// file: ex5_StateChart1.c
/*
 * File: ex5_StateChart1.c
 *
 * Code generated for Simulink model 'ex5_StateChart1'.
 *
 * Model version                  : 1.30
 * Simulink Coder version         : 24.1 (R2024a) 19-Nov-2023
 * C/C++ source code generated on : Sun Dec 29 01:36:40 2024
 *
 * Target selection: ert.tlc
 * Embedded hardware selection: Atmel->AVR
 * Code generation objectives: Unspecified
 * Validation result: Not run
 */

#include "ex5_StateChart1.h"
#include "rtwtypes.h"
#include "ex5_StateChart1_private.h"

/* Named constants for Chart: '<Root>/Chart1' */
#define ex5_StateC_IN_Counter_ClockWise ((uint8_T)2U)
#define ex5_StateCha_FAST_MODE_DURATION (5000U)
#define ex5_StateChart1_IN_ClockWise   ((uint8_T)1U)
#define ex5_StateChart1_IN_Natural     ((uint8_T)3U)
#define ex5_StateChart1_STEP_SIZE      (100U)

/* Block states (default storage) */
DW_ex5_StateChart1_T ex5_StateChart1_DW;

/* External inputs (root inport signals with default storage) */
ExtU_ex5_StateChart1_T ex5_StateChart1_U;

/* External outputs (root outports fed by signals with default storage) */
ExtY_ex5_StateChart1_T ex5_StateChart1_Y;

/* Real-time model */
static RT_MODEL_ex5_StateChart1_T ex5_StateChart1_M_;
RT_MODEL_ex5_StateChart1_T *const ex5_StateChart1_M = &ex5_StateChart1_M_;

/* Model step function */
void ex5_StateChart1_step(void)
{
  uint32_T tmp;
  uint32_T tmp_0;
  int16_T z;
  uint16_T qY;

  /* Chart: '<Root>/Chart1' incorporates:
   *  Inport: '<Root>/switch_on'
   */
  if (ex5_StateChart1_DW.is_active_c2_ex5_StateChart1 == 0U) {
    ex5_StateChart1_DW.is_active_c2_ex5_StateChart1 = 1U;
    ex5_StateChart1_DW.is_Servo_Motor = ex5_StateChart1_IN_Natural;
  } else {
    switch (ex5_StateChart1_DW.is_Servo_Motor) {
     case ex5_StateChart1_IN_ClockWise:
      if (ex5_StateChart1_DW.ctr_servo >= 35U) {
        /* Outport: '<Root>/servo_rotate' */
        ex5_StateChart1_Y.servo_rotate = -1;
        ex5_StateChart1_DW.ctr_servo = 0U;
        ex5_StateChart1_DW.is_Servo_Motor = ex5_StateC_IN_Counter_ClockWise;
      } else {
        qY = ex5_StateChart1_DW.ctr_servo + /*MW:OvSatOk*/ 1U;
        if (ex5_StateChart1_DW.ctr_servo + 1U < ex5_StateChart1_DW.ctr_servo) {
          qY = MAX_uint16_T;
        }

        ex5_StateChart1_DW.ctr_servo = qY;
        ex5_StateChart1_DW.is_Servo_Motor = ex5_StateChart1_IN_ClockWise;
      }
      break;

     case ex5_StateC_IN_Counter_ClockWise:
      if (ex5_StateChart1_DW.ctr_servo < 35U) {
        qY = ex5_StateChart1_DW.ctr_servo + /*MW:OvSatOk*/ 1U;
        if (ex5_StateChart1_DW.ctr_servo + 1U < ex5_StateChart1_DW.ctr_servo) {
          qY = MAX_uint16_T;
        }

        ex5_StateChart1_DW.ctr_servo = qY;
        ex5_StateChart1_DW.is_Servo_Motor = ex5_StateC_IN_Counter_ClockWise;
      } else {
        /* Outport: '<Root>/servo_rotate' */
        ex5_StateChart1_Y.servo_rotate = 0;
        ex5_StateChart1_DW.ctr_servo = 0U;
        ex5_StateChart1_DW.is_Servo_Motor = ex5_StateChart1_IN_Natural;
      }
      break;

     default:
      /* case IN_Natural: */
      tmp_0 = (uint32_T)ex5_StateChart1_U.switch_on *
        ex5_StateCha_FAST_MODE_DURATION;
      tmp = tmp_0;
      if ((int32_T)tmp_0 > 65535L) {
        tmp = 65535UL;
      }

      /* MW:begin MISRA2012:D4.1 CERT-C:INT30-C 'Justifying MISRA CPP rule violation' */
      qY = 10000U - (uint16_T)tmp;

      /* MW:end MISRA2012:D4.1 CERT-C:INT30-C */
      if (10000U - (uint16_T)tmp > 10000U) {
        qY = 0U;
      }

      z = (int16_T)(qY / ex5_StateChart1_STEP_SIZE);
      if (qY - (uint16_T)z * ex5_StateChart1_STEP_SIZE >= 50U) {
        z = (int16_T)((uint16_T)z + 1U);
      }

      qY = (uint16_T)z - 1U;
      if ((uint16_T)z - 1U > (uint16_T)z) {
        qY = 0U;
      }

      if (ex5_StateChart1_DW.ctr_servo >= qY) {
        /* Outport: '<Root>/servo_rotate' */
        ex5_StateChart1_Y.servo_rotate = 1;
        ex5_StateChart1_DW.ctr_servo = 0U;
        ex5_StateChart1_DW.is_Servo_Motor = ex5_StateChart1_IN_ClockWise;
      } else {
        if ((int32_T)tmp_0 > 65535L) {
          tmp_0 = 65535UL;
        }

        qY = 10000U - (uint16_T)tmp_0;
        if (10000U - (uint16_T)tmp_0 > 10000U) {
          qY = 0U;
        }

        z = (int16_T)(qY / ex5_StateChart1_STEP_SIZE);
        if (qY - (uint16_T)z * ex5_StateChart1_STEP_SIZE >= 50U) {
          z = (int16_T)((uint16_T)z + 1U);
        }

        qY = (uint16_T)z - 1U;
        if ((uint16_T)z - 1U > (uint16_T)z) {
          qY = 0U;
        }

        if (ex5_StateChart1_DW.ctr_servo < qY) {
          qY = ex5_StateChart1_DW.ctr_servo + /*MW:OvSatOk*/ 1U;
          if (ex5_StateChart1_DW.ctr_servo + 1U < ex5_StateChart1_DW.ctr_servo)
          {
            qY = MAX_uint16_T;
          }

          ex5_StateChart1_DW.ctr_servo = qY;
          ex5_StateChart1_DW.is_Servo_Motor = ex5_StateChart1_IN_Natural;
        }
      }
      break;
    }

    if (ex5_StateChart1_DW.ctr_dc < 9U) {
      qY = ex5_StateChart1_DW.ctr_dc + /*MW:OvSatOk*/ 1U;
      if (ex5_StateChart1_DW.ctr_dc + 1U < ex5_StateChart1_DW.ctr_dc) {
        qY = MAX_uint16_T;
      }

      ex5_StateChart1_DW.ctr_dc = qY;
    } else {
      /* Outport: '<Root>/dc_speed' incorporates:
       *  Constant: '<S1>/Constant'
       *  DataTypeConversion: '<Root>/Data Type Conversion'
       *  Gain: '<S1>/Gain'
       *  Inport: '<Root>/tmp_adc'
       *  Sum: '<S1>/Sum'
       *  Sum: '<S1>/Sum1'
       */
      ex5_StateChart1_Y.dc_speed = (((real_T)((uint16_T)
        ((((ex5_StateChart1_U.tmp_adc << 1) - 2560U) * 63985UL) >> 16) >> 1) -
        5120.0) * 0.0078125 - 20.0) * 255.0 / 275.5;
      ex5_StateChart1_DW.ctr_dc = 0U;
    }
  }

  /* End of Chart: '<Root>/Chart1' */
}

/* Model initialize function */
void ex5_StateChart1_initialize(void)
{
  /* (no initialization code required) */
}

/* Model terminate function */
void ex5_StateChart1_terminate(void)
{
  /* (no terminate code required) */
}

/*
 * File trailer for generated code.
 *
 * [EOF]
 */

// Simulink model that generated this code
simulink model "ex5_StateChart1"  (R2024a)
settings: Solver=FixedStepDiscrete  StartTime=0.0  StopTime=20.0  FixedStep=0.1  RelTol=1e-3

== system ex5_StateChart1 ==
  switch_on : Inport
  tmp_adc : Inport  Port=2
  CelsiusScaler Subsystem : Subsystem
  Chart1 : Stateflow chart  TreatAsAtomicUnit=on
  Data Type Conversion : DataTypeConversion  OutDataTypeStr=double  SaturateOnIntegerOverflow=off  RndMeth=Floor
  servo_rotate : Outport
  dc_speed : Outport  Port=2
  wires:
  CelsiusScaler Subsystem/1(celsius) -> Data Type Conversion/1
  Data Type Conversion/1 -> Chart1/2(celsius)
  tmp_adc/1 -> CelsiusScaler Subsystem/1(tmp_adc)
  switch_on/1 -> Chart1/1(switch_on)
  Chart1/1(servo_rotate) -> servo_rotate/1
  Chart1/2(dc_speed) -> dc_speed/1

== system ex5_StateChart1/CelsiusScaler Subsystem ==
  tmp_adc : Inport  OutDataTypeStr=fixdt(0,16,6)
  Constant : Constant  Value=20  OutDataTypeStr=fixdt(0,16,11)
  Constant1 : Constant  Value=-40  OutDataTypeStr=fixdt(1,16,9)
  Gain : Gain  Gain=165/338  OutDataTypeStr=fixdt(0,16,8)
  Sum : Sum  Inputs=|+-  OutDataTypeStr=fixdt(0,16,7)
  Sum1 : Sum  Inputs=|++  OutDataTypeStr=fixdt(1,16,7)
  celsius : Outport
  wires:
  Constant/1 -> Sum/2
  tmp_adc/1 -> Sum/1
  Constant1/1 -> Sum1/2
  Gain/1 -> Sum1/1
  Sum1/1 -> celsius/1
  Sum/1 -> Gain/1

== stateflow chart ex5_StateChart1/Chart1 ==
  state DC_Motor [parallel]
    settings: executionOrder=2
    state check
    check -> check [order 1] : [ctr_dc < (DC_PERIOD / STEP_SIZE) - 1]{ctr_dc = ctr_dc + 1}
    (default) -> check
    check -> check [order 2] : [ctr_dc >= (DC_PERIOD / STEP_SIZE) - 1]{dc_speed = (celsius - 20) * 255 / (16530 / 60); ctr_dc = 0;}
  state Servo_Motor [parallel]
    settings: executionOrder=1
    state Natural
    state ClockWise
    state Counter_ClockWise
    (default) -> Natural
    Natural -> Natural [order 2] : [ctr_servo < ((SLOW_MODE_DURATION - (switch_on * (SLOW_MODE_DURATION - FAST_MODE_DURATION))) / STEP_SIZE) - 1]{ctr_servo = ctr_servo + 1}
    Counter_ClockWise -> Natural [order 2] : [ctr_servo >= (SERVO_MAX_ANGLE / SERVO_ANGLE_CHANGE) - 1]{servo_rotate = 0; ctr_servo = 0}
    Natural -> ClockWise [order 1] : [ctr_servo >= ((SLOW_MODE_DURATION - (switch_on * (SLOW_MODE_DURATION - FAST_MODE_DURATION))) / STEP_SIZE) - 1]{servo_rotate = 1; ctr_servo = 0}
    ClockWise -> ClockWise [order 2] : [ctr_servo < (SERVO_MAX_ANGLE / SERVO_ANGLE_CHANGE) - 1]{ctr_servo = ctr_servo + 1}
    ClockWise -> Counter_ClockWise [order 1] : [ctr_servo >= (SERVO_MAX_ANGLE / SERVO_ANGLE_CHANGE) - 1]{servo_rotate = -1; ctr_servo = 0}
    Counter_ClockWise -> Counter_ClockWise [order 1] : [ctr_servo < (SERVO_MAX_ANGLE / SERVO_ANGLE_CHANGE) - 1]{ctr_servo = ctr_servo + 1}
  data: SLOW_MODE_DURATION constant uint16 =10000; servo_rotate output int16 =0; FAST_MODE_DURATION constant uint16 =5000; STEP_SIZE constant uint16 =100; switch_on input uint16; ctr_dc local uint16 =0; ctr_servo local uint16 =0; SERVO_MAX_ANGLE constant uint16 =180; SERVO_ANGLE_CHANGE constant uint16 =5; DC_PERIOD constant uint16 =1000; dc_speed output double =0; celsius input double
